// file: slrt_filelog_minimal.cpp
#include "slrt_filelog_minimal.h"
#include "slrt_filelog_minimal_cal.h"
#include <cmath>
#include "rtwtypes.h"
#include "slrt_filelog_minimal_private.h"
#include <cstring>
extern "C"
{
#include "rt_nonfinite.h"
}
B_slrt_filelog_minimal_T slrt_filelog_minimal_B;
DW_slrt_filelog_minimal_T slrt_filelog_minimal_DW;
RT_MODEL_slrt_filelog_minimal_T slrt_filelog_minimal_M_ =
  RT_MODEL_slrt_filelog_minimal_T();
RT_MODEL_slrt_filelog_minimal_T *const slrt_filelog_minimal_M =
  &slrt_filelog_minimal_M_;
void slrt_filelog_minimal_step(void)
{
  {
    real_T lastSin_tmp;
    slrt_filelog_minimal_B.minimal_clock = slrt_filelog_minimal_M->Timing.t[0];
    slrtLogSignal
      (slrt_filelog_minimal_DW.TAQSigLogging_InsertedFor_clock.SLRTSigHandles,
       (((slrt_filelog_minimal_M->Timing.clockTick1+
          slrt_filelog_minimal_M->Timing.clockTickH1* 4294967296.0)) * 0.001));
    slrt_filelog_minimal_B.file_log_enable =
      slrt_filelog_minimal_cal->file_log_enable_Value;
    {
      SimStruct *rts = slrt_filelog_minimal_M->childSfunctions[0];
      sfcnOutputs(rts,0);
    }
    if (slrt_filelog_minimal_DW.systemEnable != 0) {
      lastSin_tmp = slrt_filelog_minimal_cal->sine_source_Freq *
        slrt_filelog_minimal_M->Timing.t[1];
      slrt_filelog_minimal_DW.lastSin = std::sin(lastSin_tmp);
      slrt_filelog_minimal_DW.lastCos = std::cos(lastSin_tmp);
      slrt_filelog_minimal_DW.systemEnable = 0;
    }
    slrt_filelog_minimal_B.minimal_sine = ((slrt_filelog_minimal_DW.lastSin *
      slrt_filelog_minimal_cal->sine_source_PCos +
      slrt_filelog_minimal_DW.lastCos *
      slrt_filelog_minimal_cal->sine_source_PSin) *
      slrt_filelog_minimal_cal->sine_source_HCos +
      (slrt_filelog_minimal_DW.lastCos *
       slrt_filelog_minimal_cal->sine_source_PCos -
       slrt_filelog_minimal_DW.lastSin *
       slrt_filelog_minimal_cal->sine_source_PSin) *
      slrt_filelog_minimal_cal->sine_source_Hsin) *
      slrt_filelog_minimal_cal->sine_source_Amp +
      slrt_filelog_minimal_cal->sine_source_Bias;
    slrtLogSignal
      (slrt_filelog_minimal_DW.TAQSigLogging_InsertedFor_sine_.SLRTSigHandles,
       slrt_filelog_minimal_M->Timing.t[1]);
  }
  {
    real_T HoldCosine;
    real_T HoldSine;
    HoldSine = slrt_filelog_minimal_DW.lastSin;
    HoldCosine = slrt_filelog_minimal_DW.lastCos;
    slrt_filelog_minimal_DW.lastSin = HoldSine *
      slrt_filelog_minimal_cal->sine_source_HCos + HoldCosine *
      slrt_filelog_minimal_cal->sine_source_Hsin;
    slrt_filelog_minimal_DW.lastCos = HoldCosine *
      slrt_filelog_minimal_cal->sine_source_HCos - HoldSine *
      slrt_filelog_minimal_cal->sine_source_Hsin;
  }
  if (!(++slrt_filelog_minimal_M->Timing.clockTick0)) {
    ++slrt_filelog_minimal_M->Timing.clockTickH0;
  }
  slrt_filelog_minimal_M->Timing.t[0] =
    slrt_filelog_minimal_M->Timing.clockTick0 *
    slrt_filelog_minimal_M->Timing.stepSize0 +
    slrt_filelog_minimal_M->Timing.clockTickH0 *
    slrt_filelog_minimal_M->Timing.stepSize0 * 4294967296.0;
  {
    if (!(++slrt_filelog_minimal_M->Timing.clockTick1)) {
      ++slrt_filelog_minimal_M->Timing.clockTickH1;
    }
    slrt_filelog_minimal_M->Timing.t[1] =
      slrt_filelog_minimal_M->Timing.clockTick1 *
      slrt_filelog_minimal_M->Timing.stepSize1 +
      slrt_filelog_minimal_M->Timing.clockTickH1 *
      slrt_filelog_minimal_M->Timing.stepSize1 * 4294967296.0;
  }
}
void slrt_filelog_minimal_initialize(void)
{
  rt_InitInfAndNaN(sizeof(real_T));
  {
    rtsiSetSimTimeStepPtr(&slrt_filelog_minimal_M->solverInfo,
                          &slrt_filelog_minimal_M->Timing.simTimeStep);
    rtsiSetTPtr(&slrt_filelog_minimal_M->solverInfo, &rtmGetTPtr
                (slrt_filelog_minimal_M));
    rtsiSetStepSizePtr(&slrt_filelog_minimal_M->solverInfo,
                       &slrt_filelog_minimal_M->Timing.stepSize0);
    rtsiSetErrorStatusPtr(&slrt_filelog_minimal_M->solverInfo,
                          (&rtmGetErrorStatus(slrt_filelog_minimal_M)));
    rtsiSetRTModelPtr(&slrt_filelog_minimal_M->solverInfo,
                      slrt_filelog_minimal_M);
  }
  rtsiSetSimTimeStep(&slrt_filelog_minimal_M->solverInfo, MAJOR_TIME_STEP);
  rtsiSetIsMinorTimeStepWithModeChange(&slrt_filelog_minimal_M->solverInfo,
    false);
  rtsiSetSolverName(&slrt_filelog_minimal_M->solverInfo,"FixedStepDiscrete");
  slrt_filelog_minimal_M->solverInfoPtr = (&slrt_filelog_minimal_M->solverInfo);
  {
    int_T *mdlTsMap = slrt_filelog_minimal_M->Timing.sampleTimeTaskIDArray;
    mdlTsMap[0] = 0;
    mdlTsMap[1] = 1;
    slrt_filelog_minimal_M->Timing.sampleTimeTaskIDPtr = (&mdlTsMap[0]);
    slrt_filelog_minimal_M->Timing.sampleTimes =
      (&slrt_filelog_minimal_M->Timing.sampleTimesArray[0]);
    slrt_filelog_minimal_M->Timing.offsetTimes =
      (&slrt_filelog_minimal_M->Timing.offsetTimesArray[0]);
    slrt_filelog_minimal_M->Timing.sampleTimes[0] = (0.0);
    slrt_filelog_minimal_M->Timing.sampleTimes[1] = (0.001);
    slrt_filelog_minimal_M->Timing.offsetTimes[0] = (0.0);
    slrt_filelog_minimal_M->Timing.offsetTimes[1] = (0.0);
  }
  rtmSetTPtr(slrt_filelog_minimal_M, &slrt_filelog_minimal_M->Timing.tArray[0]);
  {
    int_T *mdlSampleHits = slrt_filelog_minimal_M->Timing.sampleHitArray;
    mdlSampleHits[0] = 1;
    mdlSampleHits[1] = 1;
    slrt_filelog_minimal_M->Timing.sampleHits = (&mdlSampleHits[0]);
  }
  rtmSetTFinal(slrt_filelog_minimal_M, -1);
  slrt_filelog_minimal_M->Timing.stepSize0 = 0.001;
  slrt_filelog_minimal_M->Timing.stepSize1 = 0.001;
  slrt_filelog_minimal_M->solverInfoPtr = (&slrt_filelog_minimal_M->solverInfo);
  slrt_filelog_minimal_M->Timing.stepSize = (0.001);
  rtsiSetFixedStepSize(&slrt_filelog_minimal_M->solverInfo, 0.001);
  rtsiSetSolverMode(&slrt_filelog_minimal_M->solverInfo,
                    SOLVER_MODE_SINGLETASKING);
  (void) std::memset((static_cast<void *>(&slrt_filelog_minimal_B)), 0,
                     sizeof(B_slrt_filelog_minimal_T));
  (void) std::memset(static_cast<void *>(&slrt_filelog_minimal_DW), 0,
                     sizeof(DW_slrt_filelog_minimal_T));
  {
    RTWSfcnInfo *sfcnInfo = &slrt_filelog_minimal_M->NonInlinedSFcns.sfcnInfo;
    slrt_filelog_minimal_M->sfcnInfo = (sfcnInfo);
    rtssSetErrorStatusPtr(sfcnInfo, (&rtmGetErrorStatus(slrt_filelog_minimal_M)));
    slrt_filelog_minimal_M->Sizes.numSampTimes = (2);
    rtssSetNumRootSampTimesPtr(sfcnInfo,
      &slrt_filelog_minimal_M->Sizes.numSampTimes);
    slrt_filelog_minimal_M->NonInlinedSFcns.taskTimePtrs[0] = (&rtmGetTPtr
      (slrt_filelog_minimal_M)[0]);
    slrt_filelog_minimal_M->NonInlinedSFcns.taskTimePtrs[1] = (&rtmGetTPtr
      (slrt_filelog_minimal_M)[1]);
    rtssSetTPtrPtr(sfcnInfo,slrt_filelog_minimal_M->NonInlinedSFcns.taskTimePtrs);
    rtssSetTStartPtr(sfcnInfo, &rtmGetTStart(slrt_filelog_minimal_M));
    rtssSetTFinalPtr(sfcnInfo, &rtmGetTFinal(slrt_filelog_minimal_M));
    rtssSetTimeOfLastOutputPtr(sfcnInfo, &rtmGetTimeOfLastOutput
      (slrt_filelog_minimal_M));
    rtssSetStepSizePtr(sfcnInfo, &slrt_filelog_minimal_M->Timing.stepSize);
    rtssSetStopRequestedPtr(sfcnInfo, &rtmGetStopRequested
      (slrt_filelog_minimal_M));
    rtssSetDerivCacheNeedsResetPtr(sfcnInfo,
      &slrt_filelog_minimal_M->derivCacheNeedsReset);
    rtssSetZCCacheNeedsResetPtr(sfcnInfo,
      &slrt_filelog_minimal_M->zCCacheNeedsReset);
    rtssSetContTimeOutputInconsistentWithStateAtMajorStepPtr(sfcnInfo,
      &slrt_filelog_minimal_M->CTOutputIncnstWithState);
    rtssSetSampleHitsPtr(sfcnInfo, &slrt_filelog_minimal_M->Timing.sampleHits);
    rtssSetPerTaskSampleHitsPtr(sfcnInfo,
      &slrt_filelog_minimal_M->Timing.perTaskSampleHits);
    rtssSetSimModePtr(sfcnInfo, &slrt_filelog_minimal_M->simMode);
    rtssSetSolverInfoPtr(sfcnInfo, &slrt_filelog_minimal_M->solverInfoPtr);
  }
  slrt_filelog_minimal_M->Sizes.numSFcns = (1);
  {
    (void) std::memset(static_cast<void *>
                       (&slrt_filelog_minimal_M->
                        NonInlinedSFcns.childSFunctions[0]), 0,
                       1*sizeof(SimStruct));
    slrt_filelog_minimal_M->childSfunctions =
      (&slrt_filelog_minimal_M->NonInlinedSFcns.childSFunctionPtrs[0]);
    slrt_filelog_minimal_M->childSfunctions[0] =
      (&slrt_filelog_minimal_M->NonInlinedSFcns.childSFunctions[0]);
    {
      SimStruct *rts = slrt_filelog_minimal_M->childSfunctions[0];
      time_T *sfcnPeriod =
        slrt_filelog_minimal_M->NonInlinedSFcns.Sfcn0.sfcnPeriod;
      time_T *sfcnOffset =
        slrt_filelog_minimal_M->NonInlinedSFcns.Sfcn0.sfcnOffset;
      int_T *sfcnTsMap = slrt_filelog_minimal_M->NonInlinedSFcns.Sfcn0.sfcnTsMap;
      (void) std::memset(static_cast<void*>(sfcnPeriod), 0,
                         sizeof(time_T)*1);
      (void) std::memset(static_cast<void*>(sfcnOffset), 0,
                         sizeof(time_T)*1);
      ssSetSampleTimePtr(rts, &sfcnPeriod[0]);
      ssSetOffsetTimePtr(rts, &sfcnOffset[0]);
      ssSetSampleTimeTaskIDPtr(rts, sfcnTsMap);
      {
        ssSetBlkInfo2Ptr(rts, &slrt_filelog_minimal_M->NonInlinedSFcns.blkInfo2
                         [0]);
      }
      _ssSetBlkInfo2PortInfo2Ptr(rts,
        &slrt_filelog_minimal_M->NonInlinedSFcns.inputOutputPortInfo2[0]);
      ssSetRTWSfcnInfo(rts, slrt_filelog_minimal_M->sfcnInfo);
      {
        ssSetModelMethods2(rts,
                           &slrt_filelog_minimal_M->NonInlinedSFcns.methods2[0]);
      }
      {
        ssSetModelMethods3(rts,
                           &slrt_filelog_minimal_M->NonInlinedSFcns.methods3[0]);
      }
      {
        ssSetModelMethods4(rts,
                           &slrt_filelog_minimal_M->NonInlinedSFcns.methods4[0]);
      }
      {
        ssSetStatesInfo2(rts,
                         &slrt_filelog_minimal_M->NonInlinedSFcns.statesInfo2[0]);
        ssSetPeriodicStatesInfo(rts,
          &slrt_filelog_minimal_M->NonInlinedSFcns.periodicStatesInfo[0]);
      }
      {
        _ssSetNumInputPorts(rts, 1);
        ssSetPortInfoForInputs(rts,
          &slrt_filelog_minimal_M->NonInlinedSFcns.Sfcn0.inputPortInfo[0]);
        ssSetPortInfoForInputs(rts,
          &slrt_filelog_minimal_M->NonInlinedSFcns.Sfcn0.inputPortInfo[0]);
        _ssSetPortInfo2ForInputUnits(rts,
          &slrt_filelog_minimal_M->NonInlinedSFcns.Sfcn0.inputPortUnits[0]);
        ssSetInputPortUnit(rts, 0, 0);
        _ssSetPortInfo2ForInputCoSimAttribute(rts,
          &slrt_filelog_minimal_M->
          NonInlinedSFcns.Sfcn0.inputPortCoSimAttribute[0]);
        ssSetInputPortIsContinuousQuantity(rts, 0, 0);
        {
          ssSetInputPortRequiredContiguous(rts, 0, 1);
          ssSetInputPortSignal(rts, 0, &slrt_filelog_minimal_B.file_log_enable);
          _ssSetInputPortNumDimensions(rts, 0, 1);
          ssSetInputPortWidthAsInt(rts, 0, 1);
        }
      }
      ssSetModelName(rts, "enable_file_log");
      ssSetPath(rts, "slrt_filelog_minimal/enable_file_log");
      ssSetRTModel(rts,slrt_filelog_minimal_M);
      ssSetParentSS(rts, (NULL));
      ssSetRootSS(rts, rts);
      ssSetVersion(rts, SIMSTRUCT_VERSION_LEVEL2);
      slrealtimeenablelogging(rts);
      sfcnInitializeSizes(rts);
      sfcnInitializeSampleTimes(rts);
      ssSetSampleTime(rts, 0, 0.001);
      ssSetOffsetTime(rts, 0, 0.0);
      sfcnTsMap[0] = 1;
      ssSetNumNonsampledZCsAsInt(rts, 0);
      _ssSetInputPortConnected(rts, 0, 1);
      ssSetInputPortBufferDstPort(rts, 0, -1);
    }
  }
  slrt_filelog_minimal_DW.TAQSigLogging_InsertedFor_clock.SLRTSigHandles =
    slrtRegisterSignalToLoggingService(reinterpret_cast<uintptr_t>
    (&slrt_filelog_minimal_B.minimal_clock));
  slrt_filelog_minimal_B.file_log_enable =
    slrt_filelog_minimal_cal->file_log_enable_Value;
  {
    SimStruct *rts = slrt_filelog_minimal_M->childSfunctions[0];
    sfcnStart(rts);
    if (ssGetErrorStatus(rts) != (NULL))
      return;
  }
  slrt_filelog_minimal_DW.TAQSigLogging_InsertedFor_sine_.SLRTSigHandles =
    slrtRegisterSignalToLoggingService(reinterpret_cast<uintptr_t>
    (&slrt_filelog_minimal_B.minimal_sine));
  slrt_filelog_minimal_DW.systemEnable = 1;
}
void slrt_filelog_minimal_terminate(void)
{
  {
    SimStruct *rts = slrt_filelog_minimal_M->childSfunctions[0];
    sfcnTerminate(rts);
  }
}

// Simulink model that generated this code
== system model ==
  FileLog#1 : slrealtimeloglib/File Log  <- 1: Clock#1
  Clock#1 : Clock
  enable_file_log : slrealtimeloglib/Enable File Log  <- 1: file_log_enable
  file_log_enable : Constant  Value=true
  FileLog#2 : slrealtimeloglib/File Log  <- 1: sine_source
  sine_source : Sin  Frequency=2*pi*1
